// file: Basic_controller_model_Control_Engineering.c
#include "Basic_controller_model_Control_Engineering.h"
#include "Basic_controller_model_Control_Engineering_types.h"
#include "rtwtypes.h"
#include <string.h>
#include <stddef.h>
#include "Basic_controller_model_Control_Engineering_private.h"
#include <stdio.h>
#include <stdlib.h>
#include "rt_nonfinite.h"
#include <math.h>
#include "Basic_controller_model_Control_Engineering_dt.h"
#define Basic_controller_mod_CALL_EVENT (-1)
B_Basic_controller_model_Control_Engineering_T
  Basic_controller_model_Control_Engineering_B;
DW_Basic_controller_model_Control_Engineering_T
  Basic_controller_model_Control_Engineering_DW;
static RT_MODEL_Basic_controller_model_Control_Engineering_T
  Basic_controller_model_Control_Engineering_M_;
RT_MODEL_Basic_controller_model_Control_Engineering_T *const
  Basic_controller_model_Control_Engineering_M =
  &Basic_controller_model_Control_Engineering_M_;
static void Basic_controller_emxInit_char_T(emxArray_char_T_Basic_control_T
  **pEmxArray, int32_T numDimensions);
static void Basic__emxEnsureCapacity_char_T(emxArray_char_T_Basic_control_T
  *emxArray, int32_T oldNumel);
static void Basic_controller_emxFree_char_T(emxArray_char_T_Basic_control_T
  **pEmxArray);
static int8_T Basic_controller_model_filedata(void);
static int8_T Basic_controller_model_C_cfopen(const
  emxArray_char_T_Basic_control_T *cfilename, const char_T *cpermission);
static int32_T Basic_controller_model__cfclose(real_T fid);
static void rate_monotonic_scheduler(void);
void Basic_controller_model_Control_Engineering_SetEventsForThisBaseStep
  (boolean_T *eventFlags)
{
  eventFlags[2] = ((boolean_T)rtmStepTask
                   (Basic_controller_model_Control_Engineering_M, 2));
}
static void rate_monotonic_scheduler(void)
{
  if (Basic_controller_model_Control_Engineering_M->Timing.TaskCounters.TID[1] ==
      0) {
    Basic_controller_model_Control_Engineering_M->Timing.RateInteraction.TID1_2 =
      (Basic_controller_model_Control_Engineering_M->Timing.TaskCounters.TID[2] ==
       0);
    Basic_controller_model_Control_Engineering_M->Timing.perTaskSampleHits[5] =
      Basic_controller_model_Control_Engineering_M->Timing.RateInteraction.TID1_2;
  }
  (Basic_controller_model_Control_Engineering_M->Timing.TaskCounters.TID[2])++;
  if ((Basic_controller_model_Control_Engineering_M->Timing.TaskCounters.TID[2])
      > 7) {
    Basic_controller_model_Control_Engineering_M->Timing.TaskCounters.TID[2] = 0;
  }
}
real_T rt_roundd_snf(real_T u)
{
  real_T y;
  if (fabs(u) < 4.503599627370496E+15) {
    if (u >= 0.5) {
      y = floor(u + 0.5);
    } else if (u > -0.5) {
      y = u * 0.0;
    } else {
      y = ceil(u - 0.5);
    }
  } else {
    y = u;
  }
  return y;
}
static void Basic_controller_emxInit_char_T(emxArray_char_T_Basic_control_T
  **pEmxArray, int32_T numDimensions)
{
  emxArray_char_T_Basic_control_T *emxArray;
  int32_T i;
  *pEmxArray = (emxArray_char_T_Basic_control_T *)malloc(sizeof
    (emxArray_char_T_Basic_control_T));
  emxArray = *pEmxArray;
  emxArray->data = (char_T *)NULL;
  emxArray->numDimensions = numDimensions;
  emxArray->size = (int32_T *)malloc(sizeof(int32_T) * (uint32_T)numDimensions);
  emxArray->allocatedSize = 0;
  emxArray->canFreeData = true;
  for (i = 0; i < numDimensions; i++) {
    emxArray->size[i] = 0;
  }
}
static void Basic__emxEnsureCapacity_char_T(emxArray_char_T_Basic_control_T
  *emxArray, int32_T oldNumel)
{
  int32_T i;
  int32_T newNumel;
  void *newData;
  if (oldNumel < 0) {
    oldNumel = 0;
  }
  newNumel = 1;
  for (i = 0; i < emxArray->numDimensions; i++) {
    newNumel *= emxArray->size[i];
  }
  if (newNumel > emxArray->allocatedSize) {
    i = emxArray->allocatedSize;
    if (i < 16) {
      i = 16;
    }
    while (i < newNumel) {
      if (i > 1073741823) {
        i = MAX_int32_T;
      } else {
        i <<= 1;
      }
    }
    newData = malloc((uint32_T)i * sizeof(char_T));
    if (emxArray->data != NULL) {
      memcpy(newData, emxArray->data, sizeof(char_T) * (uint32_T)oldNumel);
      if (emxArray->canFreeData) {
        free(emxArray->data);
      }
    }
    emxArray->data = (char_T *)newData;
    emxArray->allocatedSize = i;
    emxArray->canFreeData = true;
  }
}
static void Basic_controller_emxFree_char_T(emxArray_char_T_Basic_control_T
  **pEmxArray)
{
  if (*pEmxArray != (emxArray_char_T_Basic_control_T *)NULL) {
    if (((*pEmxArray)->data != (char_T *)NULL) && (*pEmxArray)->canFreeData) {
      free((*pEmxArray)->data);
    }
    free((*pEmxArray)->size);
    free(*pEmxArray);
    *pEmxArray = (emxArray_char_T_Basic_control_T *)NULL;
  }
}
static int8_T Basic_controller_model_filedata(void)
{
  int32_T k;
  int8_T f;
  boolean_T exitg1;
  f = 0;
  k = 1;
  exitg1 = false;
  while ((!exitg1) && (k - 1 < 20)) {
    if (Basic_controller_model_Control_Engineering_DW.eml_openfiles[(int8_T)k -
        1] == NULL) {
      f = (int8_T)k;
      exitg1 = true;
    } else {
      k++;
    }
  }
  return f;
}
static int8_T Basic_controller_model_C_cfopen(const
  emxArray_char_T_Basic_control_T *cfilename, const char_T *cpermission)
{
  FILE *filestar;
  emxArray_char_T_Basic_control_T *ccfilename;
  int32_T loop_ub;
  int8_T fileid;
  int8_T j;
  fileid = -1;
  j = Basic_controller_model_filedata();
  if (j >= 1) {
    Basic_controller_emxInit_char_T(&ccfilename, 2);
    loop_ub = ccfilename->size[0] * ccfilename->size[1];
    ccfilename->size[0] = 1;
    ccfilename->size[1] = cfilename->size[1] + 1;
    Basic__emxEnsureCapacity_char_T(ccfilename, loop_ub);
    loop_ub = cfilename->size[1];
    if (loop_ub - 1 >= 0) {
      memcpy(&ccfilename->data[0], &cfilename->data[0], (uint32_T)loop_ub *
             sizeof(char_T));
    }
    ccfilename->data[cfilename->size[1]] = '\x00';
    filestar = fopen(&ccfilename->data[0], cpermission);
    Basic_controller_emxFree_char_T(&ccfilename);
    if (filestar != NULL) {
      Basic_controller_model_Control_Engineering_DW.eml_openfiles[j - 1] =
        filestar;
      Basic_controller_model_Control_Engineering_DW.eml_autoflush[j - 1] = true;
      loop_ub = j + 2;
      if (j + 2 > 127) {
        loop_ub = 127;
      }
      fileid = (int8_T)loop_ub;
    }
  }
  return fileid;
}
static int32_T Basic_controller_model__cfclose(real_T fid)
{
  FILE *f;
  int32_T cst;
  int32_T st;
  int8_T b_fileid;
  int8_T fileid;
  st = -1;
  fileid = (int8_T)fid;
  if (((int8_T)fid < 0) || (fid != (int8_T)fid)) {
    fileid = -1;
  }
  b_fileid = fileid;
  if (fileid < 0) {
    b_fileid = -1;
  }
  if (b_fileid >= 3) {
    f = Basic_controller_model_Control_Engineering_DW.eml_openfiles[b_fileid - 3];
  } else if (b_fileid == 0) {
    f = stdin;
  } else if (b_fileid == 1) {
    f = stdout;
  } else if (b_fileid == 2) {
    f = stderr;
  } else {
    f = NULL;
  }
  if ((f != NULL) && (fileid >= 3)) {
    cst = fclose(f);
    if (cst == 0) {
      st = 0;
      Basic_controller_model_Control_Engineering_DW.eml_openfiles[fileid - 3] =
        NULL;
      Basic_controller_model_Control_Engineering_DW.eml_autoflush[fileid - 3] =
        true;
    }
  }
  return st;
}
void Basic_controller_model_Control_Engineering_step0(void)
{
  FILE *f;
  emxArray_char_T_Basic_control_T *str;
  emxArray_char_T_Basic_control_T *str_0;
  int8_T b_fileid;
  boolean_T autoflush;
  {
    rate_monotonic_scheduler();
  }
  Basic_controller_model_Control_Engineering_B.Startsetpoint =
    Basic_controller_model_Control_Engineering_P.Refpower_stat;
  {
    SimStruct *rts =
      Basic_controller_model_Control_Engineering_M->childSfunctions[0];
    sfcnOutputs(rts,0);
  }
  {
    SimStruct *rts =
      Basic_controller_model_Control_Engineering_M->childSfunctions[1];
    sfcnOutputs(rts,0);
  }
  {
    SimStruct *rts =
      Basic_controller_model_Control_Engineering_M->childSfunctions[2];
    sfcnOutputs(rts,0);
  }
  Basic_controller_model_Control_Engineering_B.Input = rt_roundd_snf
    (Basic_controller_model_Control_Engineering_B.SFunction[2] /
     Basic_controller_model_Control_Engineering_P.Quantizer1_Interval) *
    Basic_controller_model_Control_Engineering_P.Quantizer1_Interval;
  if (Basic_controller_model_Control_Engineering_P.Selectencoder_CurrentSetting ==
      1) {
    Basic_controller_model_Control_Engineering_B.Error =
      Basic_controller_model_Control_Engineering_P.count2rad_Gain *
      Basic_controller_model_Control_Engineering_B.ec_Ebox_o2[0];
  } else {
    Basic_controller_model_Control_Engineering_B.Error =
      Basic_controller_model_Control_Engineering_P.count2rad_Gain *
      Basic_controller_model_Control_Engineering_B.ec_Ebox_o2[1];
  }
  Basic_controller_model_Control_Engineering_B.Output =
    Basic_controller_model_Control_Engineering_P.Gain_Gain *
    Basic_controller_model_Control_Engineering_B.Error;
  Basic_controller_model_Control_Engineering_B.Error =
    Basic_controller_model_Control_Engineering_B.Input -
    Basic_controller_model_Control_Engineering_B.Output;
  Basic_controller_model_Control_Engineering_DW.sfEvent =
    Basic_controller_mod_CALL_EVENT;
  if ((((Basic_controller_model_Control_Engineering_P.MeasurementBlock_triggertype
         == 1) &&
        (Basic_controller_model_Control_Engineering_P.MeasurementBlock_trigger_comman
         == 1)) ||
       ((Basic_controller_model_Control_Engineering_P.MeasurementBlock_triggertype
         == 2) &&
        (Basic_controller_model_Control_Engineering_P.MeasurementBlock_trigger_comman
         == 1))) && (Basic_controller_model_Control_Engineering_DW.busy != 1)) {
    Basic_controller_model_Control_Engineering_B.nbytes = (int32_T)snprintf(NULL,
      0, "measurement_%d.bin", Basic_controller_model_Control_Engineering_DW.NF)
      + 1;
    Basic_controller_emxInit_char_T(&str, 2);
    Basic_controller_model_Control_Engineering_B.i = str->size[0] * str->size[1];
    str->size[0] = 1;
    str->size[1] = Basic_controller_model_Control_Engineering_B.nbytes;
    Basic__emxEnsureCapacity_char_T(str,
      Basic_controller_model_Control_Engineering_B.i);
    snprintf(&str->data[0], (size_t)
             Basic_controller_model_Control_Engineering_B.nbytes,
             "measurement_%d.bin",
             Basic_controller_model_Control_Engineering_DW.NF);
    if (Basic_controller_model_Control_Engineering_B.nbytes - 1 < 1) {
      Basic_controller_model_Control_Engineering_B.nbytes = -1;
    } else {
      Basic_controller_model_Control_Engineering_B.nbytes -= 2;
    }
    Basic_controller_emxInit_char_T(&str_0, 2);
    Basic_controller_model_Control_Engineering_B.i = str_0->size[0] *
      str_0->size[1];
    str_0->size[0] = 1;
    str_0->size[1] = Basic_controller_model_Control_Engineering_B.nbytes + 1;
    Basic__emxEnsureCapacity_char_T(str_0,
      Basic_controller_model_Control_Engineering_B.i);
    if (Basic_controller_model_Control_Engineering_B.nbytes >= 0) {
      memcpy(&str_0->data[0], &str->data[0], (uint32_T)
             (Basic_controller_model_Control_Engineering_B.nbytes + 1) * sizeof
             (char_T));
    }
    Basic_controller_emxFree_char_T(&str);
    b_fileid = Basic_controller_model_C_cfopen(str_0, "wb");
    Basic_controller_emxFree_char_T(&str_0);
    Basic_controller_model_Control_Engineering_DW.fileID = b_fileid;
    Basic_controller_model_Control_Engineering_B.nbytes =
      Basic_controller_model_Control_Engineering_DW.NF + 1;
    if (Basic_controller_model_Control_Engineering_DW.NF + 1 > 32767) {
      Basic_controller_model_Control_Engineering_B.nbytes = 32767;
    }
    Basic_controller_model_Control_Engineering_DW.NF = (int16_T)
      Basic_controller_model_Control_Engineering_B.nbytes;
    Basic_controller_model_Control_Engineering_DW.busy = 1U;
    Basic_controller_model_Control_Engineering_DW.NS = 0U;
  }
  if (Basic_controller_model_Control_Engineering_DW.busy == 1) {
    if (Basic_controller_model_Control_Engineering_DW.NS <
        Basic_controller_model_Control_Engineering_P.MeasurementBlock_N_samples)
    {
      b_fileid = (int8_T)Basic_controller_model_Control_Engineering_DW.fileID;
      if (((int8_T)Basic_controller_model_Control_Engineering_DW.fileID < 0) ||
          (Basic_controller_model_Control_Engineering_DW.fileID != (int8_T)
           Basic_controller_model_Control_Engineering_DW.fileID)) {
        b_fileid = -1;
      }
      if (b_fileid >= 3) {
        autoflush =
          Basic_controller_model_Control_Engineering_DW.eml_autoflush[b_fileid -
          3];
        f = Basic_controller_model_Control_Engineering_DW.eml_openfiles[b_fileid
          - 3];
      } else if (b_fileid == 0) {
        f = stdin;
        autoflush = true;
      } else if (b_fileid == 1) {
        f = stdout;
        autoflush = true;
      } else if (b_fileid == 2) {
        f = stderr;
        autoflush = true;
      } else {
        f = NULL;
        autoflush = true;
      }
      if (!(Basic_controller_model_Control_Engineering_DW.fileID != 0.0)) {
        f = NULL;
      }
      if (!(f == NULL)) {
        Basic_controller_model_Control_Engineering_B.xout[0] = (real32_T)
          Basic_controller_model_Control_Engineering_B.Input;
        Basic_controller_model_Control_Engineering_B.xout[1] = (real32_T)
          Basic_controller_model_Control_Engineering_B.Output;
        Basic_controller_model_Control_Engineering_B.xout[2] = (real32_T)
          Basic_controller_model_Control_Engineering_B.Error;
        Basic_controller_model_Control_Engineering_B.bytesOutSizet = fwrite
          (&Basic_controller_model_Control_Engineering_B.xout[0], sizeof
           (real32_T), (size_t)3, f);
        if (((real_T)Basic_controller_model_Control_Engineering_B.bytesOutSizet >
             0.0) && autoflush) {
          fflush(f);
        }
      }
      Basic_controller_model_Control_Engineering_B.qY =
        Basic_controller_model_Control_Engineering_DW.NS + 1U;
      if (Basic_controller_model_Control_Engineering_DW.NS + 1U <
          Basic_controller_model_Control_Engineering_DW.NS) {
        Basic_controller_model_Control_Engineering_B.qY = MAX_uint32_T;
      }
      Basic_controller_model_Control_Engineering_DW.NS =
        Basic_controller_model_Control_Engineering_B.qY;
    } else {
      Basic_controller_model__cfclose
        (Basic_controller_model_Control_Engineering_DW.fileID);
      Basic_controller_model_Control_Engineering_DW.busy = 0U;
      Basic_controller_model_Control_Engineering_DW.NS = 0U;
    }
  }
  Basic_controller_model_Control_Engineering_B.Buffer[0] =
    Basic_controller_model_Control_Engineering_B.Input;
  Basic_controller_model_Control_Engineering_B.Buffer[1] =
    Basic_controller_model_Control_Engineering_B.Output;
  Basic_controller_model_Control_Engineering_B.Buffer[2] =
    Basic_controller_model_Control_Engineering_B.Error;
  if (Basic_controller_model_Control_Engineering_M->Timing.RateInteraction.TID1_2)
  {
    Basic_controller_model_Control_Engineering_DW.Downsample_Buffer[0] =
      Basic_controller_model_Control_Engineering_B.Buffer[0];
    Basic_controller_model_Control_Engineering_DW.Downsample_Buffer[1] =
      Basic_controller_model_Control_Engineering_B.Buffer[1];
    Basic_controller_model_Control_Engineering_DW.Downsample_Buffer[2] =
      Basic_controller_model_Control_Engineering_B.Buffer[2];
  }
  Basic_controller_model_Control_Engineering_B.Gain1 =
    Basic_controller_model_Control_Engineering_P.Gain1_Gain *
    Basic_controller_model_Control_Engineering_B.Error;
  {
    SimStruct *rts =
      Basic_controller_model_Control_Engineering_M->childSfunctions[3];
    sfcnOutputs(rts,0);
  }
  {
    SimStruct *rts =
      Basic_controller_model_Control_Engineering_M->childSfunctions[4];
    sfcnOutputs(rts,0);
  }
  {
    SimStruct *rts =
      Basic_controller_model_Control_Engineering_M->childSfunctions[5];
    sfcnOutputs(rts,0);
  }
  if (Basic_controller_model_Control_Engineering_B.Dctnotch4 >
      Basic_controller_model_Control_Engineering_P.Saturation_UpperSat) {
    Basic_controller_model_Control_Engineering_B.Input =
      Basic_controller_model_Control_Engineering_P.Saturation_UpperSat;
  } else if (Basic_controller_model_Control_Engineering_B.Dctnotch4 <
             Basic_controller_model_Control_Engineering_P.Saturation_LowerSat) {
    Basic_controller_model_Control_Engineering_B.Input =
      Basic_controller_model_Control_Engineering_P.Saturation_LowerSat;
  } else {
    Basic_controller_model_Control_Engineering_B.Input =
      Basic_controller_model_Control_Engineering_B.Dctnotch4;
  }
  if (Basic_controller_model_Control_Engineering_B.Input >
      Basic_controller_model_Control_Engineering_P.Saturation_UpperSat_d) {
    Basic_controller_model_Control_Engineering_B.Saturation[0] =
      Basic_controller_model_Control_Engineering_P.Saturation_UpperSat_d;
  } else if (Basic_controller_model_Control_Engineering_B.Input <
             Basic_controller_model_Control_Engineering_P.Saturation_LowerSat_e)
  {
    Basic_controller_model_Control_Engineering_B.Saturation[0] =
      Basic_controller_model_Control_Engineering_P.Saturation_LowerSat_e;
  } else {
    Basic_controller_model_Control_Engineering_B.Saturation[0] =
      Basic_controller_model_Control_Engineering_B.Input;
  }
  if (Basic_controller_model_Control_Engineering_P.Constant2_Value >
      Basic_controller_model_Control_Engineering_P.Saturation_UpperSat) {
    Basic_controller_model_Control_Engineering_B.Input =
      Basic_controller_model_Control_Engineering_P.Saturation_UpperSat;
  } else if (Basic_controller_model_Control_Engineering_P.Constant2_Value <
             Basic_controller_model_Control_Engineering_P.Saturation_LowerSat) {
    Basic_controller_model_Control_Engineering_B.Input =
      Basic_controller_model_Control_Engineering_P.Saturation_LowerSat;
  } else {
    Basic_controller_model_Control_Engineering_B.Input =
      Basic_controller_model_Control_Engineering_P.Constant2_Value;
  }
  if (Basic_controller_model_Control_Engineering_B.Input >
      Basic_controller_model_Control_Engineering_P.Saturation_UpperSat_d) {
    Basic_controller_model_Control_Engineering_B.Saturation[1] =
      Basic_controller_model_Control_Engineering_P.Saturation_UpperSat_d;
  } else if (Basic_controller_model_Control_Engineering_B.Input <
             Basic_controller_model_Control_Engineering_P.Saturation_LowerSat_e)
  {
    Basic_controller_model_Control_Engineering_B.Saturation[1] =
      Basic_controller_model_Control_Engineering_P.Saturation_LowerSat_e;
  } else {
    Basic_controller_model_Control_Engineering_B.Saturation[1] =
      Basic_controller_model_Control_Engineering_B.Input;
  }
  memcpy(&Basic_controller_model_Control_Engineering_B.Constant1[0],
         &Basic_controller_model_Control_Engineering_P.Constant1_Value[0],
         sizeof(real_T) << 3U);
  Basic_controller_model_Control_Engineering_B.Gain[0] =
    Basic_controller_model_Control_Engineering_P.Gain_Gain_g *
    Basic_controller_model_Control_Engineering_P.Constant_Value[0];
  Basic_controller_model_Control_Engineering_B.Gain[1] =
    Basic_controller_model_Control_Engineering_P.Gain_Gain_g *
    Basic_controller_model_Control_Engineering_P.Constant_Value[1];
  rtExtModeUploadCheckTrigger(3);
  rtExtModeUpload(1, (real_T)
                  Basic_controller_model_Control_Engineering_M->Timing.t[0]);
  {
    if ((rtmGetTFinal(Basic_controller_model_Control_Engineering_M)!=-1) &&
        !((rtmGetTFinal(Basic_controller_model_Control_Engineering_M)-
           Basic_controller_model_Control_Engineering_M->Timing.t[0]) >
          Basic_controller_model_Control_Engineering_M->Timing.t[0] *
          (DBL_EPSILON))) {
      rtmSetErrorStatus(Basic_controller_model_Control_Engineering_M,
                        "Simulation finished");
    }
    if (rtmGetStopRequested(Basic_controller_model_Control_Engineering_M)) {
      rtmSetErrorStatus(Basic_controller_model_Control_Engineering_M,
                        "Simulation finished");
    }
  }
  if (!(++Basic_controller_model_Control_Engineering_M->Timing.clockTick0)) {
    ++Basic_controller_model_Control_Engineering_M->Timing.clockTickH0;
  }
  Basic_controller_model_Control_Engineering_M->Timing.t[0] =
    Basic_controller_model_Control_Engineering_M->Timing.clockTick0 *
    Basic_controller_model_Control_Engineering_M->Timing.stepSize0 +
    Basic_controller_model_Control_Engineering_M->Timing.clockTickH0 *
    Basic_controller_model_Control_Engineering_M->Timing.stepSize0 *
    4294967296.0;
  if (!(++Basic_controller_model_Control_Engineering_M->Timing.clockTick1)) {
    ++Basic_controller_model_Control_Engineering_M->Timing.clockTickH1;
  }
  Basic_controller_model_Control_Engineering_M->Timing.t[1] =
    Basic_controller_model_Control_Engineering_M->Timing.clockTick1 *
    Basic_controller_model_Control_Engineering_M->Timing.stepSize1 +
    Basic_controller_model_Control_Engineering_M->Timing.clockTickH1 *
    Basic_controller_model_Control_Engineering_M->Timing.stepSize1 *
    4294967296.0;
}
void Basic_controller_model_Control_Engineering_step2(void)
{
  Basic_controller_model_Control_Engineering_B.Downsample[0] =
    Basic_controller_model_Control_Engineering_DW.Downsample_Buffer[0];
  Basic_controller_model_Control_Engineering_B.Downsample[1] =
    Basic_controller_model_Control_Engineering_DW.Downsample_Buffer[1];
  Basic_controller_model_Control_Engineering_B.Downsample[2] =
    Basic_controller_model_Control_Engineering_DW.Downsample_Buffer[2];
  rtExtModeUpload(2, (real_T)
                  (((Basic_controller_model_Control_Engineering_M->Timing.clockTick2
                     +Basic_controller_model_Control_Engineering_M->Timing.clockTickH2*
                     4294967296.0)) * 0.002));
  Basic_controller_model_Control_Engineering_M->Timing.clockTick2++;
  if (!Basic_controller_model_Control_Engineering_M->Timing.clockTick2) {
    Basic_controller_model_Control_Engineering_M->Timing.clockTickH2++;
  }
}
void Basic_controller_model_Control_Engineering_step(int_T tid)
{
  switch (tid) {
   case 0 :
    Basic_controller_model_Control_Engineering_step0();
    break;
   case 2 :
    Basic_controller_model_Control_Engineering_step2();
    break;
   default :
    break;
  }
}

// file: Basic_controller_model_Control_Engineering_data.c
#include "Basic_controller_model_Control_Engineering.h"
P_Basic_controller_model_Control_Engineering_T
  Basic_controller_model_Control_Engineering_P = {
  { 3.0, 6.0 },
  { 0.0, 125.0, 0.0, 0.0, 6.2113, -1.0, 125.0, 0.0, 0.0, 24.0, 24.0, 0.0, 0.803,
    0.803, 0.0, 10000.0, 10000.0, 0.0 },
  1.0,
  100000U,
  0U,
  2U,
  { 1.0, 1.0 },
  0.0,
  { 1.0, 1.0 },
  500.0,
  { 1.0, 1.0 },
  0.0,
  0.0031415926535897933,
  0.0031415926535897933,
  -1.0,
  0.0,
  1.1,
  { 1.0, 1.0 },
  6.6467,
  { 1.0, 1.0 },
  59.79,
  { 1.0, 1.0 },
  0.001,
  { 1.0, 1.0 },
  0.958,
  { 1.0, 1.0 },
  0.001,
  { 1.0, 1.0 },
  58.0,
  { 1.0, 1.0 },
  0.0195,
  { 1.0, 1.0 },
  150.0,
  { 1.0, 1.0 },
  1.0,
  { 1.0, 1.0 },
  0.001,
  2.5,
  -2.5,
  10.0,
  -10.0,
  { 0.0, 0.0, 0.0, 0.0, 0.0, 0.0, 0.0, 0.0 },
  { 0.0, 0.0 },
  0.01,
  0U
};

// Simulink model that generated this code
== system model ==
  MATLABFunction#1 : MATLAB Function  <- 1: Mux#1, 3: Constant#1, 4: Constant#2
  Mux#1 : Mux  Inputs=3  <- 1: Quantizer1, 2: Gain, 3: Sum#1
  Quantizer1 : Quantizer  QuantizationInterval=(2*pi)/(500*4)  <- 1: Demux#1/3
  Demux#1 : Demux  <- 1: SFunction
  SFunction : S-Function  FunctionName=ref3b  <- 1: Startsetpoint
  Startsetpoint : Constant  Value=stat
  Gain : Gain  Gain=-1  <- 1: Selectencoder
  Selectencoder : ManualSwitch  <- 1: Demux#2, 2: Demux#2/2
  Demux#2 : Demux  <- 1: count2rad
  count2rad : Gain  Gain=(2*pi)/(4*500)  <- 1: ec_Ebox/2
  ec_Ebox : S-Function  FunctionName=ec_Ebox  <- 1: Saturation, 2: Gain#1, 3: Constant1
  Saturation : Saturate  UpperLimit=10  LowerLimit=-10  <- 1: Saturate#1
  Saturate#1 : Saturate  UpperLimit=2.5  LowerLimit=-2.5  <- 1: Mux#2
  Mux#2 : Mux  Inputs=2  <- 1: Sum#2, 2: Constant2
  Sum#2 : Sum  Inputs=+  <- 1: Dctnotch4
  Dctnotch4 : S-Function  FunctionName=dnotch  <- 1: SFunction#1
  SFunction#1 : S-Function  FunctionName=dweakint  <- 1: SFunction#2
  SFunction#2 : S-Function  FunctionName=dleadlag  <- 1: Gain1
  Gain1 : Gain  Gain=1.1  <- 1: Sum#1
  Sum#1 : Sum  Inputs=+-  <- 1: Quantizer1, 2: Gain
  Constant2 : Constant  Value=0
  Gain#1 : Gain  Gain=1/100  <- 1: Constant
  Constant : Constant  Value=[0,0]
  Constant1 : Constant  Value=[0,0,0,0,0,0,0,0]
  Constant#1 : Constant  Value=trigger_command
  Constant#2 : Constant  Value=N_samples
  SFunction#3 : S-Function  FunctionName=ec_Supervisor
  Downsample : RateTransition  <- 1: Buffer
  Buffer : SignalConversion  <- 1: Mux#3
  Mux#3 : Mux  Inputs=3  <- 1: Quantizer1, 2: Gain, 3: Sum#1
== matlab function MATLABFunction#1 ==
function status = perform_measurement(u, trigger_manual, trigger_command, triggertype, N_samples)

%% Persistent variables
persistent fileID NF busy NS

% Init parameters
if isempty(NF)
    NF = int16(0);
end
if isempty(NS)
    NS = uint32(0);
end
if isempty(fileID)
    fileID = 0;
end
if isempty(busy)
    busy = uint8(0);
end

%% Check the triggers
if ( (triggertype == 0 && trigger_manual == 1) || (triggertype == 1 && trigger_command == 1) || (triggertype == 2 && (trigger_command == 1 || trigger_manual == 1) ) )
    if busy == 1
        % We are already busy, nothing to do
    else
        % We should start a new one
        fileID = fopen(sprintf('measurement_%d.bin',NF),'w');  
        NF = NF + 1;
        busy = uint8(1);
        NS = uint32(0);
    end
end

% We have started a measurement
if busy == 1
    if NS < N_samples 
        % Here we write the sample, in single precision float
        fwrite(fileID,u,'single');
        NS = NS + uint32(1);
    else
       % We have N samples already, we are done
       fclose(fileID);
       busy = uint8(0);
       NS = uint32(0);
    end
      
end
    % Output state
    status = uint8(busy);
end
